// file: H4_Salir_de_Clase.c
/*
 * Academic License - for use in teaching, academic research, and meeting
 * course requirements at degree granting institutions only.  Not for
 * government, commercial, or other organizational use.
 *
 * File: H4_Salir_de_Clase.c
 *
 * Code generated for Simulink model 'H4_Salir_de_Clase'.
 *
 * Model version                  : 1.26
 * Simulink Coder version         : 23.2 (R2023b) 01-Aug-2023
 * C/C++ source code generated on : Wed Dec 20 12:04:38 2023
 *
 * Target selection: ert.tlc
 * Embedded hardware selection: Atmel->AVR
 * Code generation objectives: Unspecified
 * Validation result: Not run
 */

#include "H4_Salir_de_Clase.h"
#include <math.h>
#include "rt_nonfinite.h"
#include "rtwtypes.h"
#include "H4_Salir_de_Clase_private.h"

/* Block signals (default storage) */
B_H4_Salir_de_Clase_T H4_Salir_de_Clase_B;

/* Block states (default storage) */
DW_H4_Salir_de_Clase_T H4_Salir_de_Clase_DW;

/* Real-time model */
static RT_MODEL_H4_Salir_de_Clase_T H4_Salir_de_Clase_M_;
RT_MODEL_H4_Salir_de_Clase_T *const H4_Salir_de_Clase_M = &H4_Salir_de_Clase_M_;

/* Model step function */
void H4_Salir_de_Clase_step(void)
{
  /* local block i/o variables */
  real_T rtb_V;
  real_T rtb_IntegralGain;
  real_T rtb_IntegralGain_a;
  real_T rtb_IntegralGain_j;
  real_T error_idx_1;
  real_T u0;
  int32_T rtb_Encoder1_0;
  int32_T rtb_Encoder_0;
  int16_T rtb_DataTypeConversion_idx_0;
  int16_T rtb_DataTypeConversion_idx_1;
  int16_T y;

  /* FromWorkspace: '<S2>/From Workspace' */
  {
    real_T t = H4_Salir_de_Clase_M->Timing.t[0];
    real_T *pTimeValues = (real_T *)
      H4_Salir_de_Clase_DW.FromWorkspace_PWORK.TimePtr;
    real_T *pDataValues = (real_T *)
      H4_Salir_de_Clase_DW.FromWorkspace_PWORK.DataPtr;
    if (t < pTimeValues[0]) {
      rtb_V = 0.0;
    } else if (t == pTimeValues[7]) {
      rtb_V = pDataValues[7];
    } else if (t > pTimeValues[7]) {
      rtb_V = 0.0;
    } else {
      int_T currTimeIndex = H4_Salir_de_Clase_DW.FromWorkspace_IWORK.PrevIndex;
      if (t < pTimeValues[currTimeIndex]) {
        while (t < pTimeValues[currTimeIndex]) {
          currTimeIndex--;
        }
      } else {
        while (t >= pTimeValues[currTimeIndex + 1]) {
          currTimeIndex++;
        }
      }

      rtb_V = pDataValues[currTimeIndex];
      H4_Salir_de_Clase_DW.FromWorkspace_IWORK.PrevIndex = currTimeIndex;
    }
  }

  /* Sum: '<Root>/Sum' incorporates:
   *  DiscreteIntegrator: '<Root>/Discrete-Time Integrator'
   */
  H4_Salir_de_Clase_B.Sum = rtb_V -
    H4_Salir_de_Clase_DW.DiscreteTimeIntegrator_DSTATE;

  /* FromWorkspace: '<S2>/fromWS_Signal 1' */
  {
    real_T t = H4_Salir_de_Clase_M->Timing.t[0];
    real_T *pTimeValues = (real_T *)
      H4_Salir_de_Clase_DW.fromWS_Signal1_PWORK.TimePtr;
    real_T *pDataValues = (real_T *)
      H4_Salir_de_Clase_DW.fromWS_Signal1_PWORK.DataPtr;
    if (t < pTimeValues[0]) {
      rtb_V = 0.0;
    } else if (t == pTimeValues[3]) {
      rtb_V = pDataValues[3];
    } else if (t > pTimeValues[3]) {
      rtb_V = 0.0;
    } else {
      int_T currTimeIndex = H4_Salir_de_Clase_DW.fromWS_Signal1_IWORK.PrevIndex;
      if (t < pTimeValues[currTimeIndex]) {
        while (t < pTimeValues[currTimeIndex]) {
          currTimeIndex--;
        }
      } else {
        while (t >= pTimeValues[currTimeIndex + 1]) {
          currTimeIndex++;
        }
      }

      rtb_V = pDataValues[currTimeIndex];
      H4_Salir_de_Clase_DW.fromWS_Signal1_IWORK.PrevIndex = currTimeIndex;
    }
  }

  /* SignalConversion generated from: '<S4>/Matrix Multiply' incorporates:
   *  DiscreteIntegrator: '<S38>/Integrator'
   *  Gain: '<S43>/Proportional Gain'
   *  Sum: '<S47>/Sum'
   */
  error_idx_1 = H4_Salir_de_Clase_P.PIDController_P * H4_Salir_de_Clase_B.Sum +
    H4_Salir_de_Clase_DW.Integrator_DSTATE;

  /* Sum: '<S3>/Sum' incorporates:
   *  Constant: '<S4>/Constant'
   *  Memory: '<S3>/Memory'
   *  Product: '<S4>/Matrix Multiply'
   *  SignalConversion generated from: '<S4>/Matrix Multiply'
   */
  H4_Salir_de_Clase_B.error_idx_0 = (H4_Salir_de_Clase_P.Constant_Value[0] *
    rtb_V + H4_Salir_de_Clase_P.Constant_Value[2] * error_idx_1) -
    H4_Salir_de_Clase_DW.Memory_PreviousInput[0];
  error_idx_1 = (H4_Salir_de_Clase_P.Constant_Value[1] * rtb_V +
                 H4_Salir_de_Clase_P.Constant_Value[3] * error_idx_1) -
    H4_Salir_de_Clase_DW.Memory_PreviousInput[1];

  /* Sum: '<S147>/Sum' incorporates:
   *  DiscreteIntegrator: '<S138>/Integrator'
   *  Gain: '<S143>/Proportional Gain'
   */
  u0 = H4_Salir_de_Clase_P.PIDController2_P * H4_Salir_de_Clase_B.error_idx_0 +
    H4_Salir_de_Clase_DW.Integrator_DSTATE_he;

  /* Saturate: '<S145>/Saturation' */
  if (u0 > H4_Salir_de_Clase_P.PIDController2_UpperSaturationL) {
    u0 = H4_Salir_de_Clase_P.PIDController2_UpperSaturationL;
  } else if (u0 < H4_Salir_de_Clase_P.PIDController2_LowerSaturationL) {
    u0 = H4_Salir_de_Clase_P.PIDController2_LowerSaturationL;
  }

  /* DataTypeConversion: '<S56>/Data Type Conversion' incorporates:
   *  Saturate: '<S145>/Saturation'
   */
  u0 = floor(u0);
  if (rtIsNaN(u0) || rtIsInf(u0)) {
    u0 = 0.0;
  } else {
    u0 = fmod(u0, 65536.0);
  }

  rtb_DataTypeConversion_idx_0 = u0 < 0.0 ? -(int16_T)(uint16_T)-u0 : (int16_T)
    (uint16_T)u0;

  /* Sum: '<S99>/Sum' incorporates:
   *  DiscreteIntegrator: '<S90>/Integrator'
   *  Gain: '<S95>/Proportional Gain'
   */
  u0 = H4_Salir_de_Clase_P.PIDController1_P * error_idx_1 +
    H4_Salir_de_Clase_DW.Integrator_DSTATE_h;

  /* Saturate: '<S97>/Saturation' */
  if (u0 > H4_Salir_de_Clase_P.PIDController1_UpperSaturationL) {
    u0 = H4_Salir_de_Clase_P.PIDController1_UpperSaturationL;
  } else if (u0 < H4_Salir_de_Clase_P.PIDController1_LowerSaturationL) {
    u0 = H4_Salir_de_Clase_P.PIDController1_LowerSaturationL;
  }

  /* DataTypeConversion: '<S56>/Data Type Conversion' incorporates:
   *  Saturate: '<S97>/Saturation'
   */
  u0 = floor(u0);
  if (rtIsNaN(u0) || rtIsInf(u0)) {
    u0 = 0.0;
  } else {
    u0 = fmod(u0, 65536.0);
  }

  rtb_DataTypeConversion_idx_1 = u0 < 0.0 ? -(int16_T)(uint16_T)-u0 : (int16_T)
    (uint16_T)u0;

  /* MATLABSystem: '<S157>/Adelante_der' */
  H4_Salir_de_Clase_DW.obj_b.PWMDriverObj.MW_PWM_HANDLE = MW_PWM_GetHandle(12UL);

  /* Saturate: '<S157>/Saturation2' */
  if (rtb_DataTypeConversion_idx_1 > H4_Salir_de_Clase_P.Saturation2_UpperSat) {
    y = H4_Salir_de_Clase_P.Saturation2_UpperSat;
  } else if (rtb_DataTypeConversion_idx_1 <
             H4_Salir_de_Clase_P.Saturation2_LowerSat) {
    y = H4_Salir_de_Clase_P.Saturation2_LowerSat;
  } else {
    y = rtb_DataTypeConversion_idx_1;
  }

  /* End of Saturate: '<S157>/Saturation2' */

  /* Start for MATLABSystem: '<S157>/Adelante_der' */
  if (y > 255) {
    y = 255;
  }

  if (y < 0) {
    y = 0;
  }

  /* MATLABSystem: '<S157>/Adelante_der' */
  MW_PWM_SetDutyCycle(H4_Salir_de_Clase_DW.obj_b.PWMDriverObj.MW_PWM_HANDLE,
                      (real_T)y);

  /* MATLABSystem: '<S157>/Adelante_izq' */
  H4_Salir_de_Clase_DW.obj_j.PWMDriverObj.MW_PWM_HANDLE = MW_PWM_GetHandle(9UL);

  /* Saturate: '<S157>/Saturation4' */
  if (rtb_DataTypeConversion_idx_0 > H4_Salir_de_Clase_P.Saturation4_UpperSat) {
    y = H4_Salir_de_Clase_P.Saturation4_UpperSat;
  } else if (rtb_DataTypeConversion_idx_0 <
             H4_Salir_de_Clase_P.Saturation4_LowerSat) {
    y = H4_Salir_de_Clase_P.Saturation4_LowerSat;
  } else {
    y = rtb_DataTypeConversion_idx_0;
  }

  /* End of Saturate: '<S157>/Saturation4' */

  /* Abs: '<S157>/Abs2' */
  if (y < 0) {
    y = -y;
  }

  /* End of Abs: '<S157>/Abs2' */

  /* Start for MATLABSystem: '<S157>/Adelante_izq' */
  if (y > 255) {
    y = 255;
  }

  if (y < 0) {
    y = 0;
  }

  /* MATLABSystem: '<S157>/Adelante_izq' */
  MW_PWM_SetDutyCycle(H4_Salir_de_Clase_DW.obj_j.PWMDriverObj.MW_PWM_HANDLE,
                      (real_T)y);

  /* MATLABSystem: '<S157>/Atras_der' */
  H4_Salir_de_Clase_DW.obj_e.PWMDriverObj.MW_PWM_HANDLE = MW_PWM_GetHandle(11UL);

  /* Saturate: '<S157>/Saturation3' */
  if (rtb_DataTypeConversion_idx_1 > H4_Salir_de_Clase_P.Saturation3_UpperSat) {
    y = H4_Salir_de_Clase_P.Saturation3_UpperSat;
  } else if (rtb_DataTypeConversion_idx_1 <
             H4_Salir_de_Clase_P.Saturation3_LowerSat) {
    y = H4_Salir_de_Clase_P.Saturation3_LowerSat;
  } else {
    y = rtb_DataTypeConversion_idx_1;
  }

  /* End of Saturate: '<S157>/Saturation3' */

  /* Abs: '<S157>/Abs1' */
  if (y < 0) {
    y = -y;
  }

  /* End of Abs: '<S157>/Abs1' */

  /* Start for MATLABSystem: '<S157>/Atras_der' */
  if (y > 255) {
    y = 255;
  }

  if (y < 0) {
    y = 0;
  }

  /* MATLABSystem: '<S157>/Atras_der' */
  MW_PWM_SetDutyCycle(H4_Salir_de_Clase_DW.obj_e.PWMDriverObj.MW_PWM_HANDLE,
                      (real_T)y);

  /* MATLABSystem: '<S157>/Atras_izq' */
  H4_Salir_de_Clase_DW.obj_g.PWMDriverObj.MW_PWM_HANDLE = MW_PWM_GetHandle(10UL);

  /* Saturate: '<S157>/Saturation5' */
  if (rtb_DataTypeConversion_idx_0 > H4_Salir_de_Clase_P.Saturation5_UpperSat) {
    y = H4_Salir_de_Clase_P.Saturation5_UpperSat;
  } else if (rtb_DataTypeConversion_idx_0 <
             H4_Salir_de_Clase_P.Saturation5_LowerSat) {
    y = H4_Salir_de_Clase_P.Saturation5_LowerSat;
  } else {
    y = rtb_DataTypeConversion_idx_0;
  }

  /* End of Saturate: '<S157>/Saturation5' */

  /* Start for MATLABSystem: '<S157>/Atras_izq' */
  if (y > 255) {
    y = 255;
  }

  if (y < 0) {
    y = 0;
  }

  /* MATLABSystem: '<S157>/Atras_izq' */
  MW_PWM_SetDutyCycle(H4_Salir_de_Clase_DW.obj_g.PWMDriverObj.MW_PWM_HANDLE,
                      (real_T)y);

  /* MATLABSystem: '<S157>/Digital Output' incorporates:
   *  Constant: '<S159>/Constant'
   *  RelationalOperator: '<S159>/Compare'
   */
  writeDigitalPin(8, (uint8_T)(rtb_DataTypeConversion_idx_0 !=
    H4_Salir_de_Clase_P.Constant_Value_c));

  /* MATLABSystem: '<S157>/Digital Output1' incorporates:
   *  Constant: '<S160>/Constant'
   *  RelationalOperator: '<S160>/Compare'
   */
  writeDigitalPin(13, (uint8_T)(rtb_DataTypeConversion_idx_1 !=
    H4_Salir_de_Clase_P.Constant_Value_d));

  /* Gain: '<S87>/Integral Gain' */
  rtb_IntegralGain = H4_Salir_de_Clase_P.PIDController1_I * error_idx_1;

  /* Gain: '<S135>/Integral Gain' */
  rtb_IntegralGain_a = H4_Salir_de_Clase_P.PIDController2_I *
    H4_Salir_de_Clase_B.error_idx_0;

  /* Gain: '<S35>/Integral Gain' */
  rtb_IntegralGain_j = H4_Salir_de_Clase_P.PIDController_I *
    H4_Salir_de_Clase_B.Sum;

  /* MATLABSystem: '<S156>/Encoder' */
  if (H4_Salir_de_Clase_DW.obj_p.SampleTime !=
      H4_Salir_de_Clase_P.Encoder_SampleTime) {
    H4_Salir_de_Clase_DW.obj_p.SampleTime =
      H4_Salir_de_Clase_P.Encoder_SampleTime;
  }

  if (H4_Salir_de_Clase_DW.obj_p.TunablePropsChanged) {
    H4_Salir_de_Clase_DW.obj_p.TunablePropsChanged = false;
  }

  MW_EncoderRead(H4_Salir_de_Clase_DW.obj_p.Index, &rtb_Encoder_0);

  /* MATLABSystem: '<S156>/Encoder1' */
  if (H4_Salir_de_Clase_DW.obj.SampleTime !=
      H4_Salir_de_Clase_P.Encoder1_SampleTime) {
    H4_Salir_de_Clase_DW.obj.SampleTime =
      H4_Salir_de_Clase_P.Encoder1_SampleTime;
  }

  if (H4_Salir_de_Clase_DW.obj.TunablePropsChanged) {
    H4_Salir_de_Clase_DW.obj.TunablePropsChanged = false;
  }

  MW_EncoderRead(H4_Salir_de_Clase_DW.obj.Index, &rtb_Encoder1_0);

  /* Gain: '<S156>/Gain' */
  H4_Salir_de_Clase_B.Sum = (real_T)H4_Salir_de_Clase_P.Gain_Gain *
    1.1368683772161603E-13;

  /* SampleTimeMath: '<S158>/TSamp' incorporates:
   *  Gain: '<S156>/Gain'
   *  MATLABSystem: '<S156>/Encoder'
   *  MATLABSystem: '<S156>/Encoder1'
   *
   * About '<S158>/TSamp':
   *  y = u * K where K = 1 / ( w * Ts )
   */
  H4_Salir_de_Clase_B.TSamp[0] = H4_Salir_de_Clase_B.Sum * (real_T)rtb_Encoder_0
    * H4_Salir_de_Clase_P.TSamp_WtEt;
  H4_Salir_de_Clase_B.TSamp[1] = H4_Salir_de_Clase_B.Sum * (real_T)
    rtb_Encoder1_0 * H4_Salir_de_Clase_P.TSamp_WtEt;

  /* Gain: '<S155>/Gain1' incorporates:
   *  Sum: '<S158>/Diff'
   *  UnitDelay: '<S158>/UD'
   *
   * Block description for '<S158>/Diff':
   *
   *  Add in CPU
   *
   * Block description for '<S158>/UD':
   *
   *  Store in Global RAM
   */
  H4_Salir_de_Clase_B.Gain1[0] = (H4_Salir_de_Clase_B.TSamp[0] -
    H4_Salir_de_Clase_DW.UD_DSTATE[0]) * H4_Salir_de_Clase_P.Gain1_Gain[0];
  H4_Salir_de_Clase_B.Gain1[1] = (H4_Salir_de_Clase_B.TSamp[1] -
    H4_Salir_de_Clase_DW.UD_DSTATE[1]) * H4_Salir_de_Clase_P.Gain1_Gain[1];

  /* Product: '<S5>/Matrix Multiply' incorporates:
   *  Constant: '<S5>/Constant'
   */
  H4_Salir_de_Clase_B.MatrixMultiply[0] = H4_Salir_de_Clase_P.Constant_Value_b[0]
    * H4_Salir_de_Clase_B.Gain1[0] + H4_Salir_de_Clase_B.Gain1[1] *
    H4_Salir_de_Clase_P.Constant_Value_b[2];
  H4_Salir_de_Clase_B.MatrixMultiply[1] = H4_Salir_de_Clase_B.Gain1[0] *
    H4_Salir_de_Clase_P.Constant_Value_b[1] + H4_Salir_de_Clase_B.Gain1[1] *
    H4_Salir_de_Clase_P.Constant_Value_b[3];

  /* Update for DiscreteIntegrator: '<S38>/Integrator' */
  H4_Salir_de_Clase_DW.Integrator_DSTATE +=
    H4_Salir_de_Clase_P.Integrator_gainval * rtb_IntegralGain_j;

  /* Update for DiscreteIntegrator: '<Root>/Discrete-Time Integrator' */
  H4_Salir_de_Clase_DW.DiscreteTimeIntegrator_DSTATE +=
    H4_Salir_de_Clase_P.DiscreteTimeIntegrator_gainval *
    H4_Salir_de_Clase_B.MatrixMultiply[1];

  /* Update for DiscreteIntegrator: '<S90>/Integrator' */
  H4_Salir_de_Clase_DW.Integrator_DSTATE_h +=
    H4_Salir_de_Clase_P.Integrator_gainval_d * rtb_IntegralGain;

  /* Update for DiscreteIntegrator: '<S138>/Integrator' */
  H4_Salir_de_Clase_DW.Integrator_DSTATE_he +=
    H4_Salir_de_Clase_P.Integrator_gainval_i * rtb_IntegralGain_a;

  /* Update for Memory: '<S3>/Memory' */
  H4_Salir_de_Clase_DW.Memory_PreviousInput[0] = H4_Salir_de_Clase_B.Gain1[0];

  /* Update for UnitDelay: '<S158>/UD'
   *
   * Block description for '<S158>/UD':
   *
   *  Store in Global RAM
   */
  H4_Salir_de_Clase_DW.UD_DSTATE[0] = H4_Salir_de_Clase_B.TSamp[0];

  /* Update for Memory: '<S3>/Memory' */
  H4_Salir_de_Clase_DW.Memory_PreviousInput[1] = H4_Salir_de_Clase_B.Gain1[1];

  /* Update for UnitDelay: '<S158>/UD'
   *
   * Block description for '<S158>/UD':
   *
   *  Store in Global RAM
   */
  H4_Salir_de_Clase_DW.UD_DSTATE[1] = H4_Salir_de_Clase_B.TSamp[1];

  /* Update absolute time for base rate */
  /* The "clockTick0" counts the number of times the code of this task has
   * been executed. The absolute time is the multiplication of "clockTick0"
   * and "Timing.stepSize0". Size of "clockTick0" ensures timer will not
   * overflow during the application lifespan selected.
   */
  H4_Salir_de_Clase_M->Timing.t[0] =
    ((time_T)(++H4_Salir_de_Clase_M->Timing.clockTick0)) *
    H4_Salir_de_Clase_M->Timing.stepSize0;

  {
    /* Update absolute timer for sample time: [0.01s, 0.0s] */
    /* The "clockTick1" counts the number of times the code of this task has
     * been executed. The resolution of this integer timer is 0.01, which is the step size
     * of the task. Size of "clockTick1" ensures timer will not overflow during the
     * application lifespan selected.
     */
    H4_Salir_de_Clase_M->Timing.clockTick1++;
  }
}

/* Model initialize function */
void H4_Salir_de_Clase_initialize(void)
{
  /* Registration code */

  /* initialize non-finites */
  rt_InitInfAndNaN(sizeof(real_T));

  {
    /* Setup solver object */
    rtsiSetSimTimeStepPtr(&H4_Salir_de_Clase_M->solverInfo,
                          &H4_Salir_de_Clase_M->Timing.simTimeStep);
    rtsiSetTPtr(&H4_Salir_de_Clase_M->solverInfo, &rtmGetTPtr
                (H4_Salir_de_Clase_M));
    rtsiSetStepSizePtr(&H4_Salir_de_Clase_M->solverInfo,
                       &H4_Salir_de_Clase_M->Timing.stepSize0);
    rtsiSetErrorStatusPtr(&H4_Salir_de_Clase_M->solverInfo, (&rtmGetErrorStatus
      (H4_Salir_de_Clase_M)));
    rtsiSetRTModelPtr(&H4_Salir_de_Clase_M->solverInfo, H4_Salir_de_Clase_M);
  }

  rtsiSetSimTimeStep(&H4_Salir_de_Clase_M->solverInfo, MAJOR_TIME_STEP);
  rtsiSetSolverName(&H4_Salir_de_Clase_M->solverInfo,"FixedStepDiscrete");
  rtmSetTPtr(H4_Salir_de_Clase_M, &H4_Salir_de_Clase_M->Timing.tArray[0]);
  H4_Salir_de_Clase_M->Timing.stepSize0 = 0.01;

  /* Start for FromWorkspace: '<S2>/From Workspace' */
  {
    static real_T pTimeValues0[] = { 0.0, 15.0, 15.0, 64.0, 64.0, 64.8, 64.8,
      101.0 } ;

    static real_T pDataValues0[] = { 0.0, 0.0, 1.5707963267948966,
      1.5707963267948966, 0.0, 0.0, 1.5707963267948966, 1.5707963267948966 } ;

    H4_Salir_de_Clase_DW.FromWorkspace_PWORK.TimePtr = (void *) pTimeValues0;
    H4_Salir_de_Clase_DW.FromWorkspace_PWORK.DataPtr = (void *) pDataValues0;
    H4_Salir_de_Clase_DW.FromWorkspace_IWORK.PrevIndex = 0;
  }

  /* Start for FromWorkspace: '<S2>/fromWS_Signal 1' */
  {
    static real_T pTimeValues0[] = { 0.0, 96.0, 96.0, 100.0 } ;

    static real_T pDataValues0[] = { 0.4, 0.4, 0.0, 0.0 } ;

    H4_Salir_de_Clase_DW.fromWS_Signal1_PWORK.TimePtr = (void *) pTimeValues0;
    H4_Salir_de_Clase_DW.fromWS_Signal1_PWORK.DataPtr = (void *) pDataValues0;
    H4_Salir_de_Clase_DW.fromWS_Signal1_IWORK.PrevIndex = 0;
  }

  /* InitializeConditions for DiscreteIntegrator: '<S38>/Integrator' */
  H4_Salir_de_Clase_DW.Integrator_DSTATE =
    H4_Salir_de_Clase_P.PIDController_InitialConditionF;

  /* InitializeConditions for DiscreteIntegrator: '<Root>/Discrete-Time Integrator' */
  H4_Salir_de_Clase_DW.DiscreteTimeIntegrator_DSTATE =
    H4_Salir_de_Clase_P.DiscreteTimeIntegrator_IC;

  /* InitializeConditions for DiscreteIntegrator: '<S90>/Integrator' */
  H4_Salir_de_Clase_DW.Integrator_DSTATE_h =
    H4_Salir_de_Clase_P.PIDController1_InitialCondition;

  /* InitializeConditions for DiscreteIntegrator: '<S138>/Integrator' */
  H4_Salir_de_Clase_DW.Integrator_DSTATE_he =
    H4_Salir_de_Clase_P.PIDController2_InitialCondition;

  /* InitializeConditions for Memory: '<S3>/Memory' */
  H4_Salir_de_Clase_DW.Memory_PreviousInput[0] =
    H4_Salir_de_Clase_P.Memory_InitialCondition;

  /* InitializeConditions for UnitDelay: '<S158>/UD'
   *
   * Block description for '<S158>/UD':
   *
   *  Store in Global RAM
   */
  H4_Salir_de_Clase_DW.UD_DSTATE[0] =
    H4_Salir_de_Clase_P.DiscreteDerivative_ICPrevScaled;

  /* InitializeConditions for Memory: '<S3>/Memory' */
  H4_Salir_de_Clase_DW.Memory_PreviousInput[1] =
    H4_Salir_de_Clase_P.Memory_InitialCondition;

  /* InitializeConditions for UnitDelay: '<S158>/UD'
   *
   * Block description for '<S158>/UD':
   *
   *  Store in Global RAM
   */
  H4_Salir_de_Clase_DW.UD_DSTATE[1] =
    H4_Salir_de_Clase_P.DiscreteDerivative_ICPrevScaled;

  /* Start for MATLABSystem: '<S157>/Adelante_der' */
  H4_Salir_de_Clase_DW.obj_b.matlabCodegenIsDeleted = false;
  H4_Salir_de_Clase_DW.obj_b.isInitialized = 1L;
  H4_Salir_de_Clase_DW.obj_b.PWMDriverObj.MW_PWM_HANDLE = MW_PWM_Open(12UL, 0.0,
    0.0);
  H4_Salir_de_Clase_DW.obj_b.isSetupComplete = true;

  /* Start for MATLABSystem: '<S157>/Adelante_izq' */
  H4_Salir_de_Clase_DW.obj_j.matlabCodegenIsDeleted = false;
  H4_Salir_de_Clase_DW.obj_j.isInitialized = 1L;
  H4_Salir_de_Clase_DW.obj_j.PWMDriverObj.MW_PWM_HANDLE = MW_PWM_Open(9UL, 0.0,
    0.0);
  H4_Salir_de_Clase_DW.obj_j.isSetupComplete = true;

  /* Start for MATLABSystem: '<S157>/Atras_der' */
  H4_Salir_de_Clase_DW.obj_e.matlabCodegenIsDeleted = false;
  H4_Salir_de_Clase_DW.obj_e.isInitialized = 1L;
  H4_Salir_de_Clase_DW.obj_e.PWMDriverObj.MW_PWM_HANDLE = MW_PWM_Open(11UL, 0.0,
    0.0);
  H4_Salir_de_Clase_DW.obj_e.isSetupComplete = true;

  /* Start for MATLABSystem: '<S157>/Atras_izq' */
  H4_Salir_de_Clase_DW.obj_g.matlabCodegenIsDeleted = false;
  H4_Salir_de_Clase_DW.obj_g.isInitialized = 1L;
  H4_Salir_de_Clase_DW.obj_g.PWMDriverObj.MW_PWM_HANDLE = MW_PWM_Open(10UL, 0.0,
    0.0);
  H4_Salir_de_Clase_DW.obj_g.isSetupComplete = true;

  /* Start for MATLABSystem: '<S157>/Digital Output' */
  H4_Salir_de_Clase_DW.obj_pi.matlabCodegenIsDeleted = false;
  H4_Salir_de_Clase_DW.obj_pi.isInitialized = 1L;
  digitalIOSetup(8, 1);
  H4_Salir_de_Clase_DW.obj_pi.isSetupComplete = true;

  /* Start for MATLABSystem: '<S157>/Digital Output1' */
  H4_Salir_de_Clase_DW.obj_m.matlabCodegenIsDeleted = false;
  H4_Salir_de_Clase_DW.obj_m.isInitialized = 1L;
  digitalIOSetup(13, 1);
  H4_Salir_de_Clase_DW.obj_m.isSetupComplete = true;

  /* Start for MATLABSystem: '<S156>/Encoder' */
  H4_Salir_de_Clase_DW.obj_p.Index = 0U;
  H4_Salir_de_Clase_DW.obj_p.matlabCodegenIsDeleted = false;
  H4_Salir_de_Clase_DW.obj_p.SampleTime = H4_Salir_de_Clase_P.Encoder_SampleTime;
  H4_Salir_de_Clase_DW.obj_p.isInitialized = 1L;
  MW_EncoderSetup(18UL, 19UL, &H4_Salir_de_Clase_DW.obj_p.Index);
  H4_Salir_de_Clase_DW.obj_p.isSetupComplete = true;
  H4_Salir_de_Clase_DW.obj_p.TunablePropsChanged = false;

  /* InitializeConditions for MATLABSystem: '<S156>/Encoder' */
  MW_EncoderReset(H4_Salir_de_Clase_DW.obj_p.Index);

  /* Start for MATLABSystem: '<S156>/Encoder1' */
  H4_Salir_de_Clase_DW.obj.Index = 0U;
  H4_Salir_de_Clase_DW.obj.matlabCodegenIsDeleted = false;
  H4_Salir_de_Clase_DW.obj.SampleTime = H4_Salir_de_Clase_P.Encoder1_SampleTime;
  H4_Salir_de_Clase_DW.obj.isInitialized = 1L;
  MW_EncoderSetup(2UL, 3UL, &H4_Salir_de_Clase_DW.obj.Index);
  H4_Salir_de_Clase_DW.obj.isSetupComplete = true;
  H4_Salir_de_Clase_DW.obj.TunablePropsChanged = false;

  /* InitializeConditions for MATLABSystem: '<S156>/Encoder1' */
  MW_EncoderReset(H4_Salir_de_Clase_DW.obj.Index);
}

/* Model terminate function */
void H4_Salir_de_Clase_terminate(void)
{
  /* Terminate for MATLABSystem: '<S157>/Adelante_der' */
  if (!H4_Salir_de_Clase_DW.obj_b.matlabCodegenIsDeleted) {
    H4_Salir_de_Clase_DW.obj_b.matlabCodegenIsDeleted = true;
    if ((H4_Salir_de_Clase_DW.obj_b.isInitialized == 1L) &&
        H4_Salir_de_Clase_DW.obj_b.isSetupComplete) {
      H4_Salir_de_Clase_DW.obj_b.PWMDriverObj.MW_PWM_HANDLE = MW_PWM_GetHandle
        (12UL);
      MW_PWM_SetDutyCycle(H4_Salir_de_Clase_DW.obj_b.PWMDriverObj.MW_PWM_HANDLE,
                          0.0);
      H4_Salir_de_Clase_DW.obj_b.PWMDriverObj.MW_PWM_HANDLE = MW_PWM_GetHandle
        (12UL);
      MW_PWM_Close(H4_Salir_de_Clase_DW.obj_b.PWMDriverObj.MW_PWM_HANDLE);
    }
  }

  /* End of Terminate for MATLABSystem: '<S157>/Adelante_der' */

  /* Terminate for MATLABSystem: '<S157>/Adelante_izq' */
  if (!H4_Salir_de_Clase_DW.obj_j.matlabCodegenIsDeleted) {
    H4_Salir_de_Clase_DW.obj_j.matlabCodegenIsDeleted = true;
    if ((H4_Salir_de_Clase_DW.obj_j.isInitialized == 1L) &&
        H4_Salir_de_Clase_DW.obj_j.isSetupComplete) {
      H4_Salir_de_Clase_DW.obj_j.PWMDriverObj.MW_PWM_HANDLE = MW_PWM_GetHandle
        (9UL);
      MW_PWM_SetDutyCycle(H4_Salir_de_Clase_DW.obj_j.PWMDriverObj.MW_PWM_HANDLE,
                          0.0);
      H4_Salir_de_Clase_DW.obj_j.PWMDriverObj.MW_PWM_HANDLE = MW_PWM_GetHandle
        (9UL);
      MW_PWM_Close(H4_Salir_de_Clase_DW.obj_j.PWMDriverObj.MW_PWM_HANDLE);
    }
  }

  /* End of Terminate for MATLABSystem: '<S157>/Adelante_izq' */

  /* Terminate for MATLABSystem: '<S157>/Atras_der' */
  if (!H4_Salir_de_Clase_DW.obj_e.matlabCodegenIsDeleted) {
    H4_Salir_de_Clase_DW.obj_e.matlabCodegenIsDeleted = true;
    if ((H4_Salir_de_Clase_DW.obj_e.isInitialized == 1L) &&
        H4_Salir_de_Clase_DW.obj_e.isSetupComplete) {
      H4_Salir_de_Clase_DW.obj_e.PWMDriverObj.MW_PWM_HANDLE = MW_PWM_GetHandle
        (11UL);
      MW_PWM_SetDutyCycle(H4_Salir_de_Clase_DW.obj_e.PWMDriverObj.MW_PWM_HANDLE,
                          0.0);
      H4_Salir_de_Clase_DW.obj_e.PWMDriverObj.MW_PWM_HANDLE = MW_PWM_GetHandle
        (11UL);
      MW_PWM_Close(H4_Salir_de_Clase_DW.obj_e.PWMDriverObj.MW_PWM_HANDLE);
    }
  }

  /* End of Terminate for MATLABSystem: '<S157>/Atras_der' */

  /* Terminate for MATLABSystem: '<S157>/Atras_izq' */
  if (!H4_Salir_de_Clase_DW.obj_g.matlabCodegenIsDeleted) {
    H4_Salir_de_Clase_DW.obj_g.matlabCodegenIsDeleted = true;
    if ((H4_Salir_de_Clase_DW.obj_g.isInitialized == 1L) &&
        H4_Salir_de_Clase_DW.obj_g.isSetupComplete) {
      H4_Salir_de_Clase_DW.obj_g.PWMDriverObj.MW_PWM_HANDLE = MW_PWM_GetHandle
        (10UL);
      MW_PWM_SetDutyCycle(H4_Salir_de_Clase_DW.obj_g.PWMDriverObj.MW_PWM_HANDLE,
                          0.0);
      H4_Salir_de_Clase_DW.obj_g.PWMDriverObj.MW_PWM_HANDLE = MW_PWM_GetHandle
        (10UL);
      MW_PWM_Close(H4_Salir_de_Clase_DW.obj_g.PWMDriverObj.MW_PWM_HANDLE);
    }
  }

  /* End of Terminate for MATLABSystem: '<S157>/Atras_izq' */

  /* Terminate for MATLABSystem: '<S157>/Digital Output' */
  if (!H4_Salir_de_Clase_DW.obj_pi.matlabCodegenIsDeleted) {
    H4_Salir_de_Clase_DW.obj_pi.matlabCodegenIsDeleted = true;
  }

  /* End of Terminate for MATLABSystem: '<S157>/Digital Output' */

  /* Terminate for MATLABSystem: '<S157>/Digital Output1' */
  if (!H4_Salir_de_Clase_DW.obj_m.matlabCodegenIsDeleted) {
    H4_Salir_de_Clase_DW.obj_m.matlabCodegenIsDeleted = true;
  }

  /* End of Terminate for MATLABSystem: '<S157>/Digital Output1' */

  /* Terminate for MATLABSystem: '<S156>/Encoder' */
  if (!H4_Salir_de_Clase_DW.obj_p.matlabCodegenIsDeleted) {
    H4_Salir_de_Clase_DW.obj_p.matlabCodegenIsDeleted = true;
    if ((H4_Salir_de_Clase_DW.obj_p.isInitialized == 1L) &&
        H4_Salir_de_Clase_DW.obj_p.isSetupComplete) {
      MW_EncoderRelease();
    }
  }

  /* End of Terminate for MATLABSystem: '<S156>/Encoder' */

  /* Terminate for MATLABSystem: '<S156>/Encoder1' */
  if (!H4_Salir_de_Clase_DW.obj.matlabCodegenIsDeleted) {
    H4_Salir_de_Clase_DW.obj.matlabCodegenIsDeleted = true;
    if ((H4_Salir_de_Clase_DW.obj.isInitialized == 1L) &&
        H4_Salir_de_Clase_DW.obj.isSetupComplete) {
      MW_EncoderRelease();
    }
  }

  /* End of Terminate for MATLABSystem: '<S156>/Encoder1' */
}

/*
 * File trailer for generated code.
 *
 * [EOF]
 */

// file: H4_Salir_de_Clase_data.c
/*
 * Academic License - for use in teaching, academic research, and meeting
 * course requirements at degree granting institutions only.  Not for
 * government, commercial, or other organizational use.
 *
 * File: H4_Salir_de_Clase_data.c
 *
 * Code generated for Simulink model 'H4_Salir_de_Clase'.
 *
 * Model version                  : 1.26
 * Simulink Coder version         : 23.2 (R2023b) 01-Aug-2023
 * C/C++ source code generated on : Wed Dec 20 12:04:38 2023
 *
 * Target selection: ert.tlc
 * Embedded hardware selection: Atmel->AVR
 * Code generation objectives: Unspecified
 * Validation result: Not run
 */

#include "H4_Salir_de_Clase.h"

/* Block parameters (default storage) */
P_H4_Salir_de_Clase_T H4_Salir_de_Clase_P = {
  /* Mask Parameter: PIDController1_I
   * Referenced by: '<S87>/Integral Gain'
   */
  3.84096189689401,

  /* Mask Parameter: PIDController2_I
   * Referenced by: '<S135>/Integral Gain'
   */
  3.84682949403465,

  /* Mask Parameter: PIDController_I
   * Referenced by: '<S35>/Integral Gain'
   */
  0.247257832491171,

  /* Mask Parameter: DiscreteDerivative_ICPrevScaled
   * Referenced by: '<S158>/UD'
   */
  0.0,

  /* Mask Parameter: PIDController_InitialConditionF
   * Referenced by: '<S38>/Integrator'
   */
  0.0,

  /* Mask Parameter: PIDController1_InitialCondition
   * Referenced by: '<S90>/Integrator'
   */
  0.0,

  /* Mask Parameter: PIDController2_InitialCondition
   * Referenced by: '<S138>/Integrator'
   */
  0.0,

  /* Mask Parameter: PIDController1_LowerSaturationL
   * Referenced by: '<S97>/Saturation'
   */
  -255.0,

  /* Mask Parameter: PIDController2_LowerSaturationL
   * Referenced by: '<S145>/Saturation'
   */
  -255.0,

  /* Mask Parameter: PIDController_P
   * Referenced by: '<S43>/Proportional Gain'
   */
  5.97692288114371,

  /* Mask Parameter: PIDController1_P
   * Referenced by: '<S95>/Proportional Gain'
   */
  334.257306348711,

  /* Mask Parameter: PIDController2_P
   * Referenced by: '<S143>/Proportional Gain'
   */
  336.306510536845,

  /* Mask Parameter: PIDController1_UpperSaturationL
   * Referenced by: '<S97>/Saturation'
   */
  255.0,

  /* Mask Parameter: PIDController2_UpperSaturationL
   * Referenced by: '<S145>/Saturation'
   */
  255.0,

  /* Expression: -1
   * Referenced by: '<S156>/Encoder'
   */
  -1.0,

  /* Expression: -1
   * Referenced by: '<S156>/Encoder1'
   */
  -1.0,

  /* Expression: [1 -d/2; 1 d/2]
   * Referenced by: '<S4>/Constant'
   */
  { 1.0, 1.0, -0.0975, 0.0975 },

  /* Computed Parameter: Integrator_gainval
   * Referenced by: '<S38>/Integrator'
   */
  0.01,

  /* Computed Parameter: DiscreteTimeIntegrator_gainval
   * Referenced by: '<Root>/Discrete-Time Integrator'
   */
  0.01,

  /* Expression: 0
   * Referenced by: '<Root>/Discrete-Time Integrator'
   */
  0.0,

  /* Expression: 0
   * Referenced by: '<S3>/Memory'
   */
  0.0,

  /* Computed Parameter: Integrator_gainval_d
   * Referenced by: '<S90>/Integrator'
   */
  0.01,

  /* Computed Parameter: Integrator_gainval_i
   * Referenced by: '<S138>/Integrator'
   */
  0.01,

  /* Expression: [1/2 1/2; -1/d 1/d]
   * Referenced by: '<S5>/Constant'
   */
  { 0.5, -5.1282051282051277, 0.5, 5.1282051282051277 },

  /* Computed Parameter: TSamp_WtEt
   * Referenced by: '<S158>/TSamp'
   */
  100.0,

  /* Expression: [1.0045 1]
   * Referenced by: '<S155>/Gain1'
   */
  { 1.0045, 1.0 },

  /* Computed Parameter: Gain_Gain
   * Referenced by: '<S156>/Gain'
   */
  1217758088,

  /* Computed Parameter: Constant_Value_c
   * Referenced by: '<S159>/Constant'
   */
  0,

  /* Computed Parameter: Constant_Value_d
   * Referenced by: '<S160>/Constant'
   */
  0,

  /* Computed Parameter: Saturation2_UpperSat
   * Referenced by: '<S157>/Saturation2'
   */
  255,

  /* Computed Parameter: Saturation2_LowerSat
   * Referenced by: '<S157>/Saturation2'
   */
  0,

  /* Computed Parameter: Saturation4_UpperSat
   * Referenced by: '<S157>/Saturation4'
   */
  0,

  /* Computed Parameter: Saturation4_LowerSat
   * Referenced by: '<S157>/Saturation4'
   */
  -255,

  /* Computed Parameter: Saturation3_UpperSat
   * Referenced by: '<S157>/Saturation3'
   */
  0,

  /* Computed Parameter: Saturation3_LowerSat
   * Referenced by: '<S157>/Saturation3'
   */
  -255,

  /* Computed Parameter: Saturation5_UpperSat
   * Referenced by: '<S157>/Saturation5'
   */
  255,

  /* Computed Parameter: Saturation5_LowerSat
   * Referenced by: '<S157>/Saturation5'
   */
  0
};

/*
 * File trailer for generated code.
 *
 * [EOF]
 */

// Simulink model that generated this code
simulink model "H4_Salir_de_Clase"  (R2023b)
settings: Solver=FixedStepDiscrete  StartTime=0.0  StopTime=10  FixedStep=0.01  RelTol=1e-3  EnableMultiTasking=on
model workspace (MAT data in the model file):
  d = 0.195
undefined symbols (not defined in the file or in its folder): DiscIntNeverNeededParam
libraries: slpidlib x1, SignalEditorBlockLib x1

== system H4_Salir_de_Clase ==
  Demux : Demux  Outputs=2
  Discrete-Time Integrator : DiscreteIntegrator  SampleTime=-1  ICPrevOutput=DiscIntNeverNeededParam  ICPrevScaledInput=DiscIntNeverNeededParam
  Mux : Mux  Inputs=2
  PID Controller : slpidlib/PID Controller  Controller=PI  Form=Parallel  TimeDomain=Discrete-time  UseExternalTs=off  SampleTime=-1  IntegratorMethod=Forward Euler  FilterMethod=Forward Euler  ControllerParametersSource=internal  P=5.97692288114371  I=0.247257832491171  UseKiTs=off  D=0  N=100  UseFilter=on  TunerSelectOption=Transfer Function Based (PID Tuner App)  InitialConditionSource=internal  InitialConditionForIntegrator=0  InitialConditionForFilter=0  DifferentiatorICPrevScaledInput=0  ExternalReset=none  TrackingMode=off  Kt=1  LimitOutput=off  SatLimitsSource=internal  UpperSaturationLimit=inf  LowerSaturationLimit=-inf  LinearizeAsGain=on  AntiWindupMode=none  Kb=1  LimitIntegrator=off  UpperIntegratorSaturationLimit=inf  LowerIntegratorSaturationLimit=-inf  POutMin=[]  POutMax=[]  IOutMin=[]  IOutMax=[]  DOutMin=[]  DOutMax=[]  NOutMin=[]  NOutMax=[]  SumOutMin=[]  SumOutMax=[]  SaturationOutMin=[]  SaturationOutMax=[]  PParamMin=[]  PParamMax=[]  IParamMin=[]  IParamMax=[]  DParamMin=[]  DParamMax=[]  NParamMin=[]  NParamMax=[]  KbParamMin=[]  KbParamMax=[]  KtParamMin=[]  KtParamMax=[]  KbOutMin=[]  KbOutMax=[]  KtOutMin=[]  KtOutMax=[]  IntegratorOutMin=[]  IntegratorOutMax=[]  FilterOutMin=[]  FilterOutMax=[]  SumI1OutMin=[]  SumI1OutMax=[]  SumI2OutMin=[]  SumI2OutMax=[]  SumI3OutMin=[]  SumI3OutMax=[]  SumI4OutMin=[]  SumI4OutMax=[]  SumDOutMin=[]  SumDOutMax=[]  DifferentiatorOutMin=[]  DifferentiatorOutMax=[]  FilterDiffOutCoefMin=[]  FilterDiffOutCoefMax=[]  ReciprocalOutMin=[]  ReciprocalOutMax=[]  SumDenOutMin=[]  SumDenOutMax=[]  SumNumOutMin=[]  SumNumOutMax=[]  DivideOutMin=[]  DivideOutMax=[]  UdiffTsProdOutMin=[]  UdiffTsProdOutMax=[]  NTsProdOutMin=[]  NTsProdOutMax=[]  UintegralTsProdOutMin=[]  UintegralTsProdOutMax=[]  UngainTsProdOutMin=[]  UngainTsProdOutMax=[]  ClampingZeroOutDataTypeStr=Inherit: Inherit via back propagation  ClampingZeroOutMin=[]  ClampingZeroOutMax=[]  FilterDenConstantOutDataTypeStr=Inherit: Inherit via back propagation  FilterDenConstantOutMin=[]  FilterDenConstantOutMax=[]  PCopyOutDataTypeStr=Inherit: Inherit via back propagation  PCopyOutMin=[]  PCopyOutMax=[]  NCopyOutDataTypeStr=Inherit: Inherit via back propagation  NCopyOutMin=[]  NCopyOutMax=[]  IntegratorContinuousStateAttributes=''  IntegratorStateMustResolveToSignalObject=off  IntegratorRTWStateStorageClass=Auto  FilterContinuousStateAttributes=''  FilterStateMustResolveToSignalObject=off  FilterRTWStateStorageClass=Auto  ParallelPVariant=InternalParameters  IdealPVariant=Disabled  IVariant=InternalParameters  DVariant=Disabled  IntegratorVariant=Discrete  SatVariant=Disabled  AWVariant=Passthrough  PCopyVariant=Disabled  TRVariant=Disabled  FdbkBlocksVariant=Forward  IdealPFdbkVariant=Disabled  SatFdbkVariant=Disabled  DerivativeFilterVariant=Disabled  NVariant=Disabled  NCopyVariant=Disabled_SignalSpec  FilterICVariant=Disabled  IntegratorICVariant=InternalICs  ExternalResetVariant=Disabled  TRSumVariant=Passthrough  SumFdbkVariant=Disabled  SumVariant=Sum_PI  TsampFilterVariant=InternalTs  TsampNgainVariant=Passthrough  TsampIntegralVariant=Disabled_SignalSpec  ExternalSaturationOutDataTypeStr=Inherit: Same as second input
  Signal Editor : SignalEditorBlockLib/Signal Editor  FileName=Pulsos_salirclase.mat  ActiveScenario=Scenario  ActiveSignal=V  IsBus=off  OutputBusObjectStr=Bus: BusObject  SampleTime=0  Interpolate=off  ZeroCross=off  OutputAfterFinalValue=Setting to zero  Unit=inherit  PreserveSignalName=on  ApplySigPropsToAllScenarios=on  ApplySigPropsToAllSignals=on
  Subsystem Reference : Subsystem  ReferencedSubsystem=Piero_ControladoZ_memoria
  Subsystem Reference1 : Subsystem  ReferencedSubsystem=MCI2
  Subsystem Reference2 : Subsystem  ReferencedSubsystem=MCD2
  Subsystem Reference4 : Subsystem  ReferencedSubsystem=OdometriaZ
  Sum : Sum  Inputs=|+-
  Terminator : Terminator
  wires:
  Subsystem Reference1/1 -> Subsystem Reference/1
  Subsystem Reference2/1 -> Demux/1, Subsystem Reference4/1
  Subsystem Reference/1 -> Subsystem Reference2/1
  PID Controller/1 -> Mux/2  "rel"
  Mux/1 -> Subsystem Reference1/1
  Signal Editor/1 -> Mux/1
  Sum/1 -> PID Controller/1
  Signal Editor/2 -> Sum/1
  Demux/1 -> Terminator/1
  Demux/2 -> Discrete-Time Integrator/1
  Discrete-Time Integrator/1 -> Sum/2
